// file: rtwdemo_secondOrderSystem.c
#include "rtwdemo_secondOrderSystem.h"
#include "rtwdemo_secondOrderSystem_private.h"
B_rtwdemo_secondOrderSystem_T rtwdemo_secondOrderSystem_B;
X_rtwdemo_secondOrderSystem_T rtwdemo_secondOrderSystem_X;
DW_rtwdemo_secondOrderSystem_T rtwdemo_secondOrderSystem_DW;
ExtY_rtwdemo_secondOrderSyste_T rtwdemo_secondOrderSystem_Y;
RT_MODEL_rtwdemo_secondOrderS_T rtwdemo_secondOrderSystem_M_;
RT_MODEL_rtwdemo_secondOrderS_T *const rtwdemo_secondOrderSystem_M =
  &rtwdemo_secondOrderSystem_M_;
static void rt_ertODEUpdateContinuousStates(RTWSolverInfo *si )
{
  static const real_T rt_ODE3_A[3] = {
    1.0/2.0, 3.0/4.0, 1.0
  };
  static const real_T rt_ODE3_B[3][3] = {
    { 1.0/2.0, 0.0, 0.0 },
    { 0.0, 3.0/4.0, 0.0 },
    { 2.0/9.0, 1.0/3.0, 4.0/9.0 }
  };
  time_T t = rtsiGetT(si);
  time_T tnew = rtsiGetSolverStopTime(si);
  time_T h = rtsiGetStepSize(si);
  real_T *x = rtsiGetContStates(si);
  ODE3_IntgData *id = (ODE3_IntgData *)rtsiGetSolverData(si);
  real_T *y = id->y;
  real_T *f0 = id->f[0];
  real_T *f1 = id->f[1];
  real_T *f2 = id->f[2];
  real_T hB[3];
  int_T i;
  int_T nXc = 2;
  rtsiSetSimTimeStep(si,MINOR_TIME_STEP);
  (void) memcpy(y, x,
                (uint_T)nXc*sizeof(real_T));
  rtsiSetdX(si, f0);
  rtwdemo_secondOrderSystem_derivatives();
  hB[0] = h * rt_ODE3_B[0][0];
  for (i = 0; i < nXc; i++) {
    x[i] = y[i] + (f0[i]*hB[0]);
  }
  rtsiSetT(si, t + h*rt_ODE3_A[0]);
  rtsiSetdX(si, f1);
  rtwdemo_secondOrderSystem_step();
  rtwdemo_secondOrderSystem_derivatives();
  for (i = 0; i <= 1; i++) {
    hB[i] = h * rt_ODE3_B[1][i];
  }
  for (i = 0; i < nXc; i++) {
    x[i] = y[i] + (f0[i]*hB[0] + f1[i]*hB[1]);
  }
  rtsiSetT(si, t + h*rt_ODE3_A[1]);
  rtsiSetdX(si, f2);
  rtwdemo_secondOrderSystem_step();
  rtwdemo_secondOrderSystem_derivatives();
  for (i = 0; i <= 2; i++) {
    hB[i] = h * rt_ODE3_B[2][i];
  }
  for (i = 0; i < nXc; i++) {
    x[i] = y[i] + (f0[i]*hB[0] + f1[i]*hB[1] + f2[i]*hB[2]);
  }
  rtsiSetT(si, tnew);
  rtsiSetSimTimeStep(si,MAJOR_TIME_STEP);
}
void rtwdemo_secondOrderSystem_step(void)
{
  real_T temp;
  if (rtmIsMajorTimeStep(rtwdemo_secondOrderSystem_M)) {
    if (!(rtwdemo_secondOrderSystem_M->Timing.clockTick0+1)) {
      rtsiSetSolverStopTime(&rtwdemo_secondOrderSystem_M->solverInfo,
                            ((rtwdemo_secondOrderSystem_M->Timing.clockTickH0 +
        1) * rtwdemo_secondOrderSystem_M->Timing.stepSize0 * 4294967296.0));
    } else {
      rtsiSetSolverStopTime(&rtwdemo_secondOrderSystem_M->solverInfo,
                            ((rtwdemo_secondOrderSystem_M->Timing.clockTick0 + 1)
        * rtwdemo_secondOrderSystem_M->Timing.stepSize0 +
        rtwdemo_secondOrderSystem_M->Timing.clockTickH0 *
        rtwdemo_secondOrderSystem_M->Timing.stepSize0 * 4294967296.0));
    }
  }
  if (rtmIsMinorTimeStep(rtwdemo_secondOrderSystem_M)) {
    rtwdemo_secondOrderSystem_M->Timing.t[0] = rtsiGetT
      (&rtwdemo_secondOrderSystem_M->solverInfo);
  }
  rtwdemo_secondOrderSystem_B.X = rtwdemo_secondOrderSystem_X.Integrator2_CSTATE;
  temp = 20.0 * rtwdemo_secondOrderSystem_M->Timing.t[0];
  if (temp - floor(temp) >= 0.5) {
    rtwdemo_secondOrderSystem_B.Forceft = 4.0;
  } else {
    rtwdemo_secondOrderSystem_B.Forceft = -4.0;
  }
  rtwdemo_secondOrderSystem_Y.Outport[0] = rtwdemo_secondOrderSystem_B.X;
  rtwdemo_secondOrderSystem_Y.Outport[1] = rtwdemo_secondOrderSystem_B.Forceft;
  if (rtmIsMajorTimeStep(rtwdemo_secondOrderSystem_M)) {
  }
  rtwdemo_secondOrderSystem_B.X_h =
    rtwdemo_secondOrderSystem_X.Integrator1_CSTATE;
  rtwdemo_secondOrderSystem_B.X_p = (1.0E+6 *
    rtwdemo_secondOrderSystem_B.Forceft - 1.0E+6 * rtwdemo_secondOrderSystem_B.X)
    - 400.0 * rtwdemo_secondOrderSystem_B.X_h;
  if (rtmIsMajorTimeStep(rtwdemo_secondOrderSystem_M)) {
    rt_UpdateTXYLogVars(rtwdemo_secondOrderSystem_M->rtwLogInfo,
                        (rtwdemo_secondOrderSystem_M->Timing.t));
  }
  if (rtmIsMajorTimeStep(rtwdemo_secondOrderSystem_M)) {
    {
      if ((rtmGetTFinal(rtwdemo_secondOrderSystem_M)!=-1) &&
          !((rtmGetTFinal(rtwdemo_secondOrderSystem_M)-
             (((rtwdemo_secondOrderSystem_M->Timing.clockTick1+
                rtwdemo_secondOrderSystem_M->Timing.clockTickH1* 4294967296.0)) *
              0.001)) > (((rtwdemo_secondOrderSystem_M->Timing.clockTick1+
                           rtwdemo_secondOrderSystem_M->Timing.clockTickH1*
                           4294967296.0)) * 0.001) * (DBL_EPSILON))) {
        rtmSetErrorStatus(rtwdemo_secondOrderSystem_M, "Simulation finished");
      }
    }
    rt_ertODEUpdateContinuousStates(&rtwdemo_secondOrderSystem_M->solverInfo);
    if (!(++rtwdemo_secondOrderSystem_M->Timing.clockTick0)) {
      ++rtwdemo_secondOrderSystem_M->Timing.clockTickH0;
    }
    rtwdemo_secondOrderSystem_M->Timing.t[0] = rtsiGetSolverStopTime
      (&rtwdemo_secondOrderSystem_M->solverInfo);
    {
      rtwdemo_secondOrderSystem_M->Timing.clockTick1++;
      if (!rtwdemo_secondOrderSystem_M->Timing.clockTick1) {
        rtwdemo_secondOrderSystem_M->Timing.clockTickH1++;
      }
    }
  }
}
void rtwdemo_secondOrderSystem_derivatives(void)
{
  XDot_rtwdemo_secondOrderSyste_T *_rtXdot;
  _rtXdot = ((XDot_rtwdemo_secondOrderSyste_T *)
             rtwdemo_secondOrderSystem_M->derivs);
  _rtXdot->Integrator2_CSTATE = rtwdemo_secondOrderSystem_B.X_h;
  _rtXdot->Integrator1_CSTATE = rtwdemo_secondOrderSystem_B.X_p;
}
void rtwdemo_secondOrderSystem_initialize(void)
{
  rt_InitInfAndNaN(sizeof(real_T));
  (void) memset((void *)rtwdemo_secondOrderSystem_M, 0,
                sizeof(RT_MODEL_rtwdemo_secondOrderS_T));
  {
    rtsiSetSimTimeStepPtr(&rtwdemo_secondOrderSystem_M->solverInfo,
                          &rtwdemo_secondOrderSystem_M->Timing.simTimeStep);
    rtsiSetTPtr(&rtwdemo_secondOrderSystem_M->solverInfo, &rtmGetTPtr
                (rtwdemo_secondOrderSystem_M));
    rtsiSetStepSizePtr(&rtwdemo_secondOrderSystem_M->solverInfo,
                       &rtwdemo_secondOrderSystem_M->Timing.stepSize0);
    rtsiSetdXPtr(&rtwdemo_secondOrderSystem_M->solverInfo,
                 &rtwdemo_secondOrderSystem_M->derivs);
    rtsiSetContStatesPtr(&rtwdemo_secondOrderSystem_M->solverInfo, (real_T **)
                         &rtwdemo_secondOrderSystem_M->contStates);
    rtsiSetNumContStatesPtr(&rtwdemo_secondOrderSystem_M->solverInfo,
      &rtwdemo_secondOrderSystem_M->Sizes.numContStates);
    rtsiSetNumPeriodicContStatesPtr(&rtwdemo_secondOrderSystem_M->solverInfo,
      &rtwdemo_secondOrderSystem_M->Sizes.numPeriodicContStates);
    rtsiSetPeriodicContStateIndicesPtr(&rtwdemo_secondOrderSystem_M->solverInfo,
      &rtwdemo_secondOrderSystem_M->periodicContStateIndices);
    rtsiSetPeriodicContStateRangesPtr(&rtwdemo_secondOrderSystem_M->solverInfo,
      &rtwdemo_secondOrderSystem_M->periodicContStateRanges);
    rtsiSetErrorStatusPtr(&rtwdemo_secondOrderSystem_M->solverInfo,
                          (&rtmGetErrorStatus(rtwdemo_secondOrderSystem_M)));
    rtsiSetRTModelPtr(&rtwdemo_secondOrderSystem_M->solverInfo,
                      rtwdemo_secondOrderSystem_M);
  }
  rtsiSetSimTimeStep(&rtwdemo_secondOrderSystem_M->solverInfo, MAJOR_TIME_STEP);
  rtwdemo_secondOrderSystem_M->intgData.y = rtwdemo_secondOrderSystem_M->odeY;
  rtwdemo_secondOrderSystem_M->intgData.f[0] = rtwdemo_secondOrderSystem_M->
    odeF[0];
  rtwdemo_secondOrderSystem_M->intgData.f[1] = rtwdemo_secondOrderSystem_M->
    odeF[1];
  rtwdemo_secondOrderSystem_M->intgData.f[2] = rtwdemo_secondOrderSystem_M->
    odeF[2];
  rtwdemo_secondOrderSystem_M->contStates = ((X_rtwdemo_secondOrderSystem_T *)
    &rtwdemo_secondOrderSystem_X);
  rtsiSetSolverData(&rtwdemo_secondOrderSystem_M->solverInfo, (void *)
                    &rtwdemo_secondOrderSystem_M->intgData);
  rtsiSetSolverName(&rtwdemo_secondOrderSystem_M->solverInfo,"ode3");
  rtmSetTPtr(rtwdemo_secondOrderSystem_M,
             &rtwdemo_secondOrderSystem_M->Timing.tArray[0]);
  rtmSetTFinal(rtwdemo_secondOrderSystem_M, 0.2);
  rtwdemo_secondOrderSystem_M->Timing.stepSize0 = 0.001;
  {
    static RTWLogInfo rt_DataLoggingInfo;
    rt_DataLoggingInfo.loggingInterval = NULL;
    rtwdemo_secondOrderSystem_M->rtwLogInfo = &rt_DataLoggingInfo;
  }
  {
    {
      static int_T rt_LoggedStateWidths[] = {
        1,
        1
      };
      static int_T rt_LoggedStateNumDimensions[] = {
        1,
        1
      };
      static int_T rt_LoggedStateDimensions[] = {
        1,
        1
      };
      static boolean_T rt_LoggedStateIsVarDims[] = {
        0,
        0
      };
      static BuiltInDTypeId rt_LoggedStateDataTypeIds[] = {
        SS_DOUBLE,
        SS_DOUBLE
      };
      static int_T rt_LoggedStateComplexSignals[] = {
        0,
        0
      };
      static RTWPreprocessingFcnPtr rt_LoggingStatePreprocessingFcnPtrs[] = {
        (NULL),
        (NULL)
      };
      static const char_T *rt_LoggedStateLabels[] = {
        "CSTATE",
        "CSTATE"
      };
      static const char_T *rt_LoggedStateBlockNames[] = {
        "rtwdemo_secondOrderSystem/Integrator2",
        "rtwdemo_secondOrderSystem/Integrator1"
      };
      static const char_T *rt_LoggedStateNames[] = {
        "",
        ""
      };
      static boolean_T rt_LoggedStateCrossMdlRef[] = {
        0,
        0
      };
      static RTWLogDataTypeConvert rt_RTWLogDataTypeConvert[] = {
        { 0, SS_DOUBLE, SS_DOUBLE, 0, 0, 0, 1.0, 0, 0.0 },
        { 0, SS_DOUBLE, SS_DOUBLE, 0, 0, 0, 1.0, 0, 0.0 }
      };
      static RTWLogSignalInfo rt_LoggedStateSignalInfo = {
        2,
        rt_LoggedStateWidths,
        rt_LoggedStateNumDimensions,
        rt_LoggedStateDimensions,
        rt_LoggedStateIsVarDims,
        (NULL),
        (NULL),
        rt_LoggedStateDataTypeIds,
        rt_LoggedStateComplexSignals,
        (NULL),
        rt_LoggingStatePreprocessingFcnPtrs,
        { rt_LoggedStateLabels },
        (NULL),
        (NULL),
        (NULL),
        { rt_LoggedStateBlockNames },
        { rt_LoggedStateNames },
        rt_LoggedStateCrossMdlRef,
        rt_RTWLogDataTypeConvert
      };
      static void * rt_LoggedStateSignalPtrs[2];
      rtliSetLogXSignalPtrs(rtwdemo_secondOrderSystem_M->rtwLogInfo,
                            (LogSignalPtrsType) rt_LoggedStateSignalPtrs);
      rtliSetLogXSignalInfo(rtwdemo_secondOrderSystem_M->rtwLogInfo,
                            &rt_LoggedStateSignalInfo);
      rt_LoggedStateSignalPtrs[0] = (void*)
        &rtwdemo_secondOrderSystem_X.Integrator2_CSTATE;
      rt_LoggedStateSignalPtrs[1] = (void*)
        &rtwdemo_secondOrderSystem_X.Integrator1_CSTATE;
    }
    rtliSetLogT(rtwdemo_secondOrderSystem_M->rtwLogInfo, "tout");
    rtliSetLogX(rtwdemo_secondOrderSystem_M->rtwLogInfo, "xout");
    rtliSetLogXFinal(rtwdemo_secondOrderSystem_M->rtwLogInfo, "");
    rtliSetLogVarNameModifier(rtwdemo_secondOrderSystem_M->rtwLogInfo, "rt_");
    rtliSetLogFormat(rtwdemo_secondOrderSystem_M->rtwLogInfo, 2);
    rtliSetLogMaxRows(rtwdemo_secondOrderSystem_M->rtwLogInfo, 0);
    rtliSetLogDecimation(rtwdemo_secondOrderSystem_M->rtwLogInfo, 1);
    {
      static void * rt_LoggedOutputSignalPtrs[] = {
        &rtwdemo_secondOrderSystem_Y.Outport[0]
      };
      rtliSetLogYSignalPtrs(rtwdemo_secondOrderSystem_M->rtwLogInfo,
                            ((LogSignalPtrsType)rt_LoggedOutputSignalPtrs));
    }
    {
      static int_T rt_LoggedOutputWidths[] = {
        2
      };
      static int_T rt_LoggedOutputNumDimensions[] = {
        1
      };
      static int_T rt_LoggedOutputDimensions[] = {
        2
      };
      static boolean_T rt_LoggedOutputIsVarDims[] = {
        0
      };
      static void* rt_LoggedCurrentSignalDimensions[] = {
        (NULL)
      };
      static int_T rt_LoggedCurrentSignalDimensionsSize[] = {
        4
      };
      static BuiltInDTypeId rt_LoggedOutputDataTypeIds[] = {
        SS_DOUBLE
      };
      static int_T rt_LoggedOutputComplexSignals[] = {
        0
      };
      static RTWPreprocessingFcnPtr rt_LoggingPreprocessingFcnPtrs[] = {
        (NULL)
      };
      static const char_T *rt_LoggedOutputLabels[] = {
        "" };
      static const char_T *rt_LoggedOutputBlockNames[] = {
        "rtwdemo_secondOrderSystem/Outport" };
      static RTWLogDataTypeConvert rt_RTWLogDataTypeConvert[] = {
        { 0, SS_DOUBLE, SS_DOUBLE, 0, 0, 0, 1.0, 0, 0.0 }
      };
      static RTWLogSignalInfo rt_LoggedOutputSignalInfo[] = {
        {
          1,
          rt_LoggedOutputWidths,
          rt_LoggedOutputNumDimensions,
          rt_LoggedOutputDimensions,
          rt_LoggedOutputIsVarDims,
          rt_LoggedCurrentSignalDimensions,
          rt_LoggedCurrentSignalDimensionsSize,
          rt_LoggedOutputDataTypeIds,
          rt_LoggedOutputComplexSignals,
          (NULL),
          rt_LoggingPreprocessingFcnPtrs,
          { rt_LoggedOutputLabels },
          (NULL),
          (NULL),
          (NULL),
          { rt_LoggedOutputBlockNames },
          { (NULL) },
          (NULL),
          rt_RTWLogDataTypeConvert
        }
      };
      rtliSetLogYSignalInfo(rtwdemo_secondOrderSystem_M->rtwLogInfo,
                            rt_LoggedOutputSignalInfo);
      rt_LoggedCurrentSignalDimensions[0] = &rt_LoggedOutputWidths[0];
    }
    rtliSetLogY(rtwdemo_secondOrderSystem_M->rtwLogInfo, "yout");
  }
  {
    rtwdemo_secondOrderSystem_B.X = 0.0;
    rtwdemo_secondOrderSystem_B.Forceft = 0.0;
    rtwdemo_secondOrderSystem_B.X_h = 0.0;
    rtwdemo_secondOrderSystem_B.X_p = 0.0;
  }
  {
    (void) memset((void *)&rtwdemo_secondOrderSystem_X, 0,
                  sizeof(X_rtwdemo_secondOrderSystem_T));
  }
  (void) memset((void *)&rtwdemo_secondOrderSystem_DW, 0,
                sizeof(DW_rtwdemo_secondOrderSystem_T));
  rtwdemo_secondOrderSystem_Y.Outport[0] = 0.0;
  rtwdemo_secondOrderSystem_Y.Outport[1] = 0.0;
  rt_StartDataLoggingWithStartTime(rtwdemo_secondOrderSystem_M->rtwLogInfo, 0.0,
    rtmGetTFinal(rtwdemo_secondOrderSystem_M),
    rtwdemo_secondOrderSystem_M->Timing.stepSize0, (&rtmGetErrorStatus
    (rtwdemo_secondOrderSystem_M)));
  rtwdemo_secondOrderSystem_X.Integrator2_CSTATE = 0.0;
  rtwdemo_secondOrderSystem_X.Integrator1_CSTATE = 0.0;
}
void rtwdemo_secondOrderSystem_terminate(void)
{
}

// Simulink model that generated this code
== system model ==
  Outport : Outport  InitialOutput=0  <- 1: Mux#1
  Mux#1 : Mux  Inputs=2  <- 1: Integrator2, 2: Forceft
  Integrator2 : Integrator  <- 1: Integrator1
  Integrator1 : Integrator  <- 1: Sum#1
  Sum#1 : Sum  Inputs=-+-  <- 1: Gain#1, 2: Gain#2, 3: Gain#3
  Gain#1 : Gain  Gain=1000000  <- 1: Integrator2
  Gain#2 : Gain  Gain=1000000  <- 1: Forceft
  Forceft : SignalGenerator  Amplitude=4  Frequency=20
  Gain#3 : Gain  Gain=400  <- 1: Integrator1
